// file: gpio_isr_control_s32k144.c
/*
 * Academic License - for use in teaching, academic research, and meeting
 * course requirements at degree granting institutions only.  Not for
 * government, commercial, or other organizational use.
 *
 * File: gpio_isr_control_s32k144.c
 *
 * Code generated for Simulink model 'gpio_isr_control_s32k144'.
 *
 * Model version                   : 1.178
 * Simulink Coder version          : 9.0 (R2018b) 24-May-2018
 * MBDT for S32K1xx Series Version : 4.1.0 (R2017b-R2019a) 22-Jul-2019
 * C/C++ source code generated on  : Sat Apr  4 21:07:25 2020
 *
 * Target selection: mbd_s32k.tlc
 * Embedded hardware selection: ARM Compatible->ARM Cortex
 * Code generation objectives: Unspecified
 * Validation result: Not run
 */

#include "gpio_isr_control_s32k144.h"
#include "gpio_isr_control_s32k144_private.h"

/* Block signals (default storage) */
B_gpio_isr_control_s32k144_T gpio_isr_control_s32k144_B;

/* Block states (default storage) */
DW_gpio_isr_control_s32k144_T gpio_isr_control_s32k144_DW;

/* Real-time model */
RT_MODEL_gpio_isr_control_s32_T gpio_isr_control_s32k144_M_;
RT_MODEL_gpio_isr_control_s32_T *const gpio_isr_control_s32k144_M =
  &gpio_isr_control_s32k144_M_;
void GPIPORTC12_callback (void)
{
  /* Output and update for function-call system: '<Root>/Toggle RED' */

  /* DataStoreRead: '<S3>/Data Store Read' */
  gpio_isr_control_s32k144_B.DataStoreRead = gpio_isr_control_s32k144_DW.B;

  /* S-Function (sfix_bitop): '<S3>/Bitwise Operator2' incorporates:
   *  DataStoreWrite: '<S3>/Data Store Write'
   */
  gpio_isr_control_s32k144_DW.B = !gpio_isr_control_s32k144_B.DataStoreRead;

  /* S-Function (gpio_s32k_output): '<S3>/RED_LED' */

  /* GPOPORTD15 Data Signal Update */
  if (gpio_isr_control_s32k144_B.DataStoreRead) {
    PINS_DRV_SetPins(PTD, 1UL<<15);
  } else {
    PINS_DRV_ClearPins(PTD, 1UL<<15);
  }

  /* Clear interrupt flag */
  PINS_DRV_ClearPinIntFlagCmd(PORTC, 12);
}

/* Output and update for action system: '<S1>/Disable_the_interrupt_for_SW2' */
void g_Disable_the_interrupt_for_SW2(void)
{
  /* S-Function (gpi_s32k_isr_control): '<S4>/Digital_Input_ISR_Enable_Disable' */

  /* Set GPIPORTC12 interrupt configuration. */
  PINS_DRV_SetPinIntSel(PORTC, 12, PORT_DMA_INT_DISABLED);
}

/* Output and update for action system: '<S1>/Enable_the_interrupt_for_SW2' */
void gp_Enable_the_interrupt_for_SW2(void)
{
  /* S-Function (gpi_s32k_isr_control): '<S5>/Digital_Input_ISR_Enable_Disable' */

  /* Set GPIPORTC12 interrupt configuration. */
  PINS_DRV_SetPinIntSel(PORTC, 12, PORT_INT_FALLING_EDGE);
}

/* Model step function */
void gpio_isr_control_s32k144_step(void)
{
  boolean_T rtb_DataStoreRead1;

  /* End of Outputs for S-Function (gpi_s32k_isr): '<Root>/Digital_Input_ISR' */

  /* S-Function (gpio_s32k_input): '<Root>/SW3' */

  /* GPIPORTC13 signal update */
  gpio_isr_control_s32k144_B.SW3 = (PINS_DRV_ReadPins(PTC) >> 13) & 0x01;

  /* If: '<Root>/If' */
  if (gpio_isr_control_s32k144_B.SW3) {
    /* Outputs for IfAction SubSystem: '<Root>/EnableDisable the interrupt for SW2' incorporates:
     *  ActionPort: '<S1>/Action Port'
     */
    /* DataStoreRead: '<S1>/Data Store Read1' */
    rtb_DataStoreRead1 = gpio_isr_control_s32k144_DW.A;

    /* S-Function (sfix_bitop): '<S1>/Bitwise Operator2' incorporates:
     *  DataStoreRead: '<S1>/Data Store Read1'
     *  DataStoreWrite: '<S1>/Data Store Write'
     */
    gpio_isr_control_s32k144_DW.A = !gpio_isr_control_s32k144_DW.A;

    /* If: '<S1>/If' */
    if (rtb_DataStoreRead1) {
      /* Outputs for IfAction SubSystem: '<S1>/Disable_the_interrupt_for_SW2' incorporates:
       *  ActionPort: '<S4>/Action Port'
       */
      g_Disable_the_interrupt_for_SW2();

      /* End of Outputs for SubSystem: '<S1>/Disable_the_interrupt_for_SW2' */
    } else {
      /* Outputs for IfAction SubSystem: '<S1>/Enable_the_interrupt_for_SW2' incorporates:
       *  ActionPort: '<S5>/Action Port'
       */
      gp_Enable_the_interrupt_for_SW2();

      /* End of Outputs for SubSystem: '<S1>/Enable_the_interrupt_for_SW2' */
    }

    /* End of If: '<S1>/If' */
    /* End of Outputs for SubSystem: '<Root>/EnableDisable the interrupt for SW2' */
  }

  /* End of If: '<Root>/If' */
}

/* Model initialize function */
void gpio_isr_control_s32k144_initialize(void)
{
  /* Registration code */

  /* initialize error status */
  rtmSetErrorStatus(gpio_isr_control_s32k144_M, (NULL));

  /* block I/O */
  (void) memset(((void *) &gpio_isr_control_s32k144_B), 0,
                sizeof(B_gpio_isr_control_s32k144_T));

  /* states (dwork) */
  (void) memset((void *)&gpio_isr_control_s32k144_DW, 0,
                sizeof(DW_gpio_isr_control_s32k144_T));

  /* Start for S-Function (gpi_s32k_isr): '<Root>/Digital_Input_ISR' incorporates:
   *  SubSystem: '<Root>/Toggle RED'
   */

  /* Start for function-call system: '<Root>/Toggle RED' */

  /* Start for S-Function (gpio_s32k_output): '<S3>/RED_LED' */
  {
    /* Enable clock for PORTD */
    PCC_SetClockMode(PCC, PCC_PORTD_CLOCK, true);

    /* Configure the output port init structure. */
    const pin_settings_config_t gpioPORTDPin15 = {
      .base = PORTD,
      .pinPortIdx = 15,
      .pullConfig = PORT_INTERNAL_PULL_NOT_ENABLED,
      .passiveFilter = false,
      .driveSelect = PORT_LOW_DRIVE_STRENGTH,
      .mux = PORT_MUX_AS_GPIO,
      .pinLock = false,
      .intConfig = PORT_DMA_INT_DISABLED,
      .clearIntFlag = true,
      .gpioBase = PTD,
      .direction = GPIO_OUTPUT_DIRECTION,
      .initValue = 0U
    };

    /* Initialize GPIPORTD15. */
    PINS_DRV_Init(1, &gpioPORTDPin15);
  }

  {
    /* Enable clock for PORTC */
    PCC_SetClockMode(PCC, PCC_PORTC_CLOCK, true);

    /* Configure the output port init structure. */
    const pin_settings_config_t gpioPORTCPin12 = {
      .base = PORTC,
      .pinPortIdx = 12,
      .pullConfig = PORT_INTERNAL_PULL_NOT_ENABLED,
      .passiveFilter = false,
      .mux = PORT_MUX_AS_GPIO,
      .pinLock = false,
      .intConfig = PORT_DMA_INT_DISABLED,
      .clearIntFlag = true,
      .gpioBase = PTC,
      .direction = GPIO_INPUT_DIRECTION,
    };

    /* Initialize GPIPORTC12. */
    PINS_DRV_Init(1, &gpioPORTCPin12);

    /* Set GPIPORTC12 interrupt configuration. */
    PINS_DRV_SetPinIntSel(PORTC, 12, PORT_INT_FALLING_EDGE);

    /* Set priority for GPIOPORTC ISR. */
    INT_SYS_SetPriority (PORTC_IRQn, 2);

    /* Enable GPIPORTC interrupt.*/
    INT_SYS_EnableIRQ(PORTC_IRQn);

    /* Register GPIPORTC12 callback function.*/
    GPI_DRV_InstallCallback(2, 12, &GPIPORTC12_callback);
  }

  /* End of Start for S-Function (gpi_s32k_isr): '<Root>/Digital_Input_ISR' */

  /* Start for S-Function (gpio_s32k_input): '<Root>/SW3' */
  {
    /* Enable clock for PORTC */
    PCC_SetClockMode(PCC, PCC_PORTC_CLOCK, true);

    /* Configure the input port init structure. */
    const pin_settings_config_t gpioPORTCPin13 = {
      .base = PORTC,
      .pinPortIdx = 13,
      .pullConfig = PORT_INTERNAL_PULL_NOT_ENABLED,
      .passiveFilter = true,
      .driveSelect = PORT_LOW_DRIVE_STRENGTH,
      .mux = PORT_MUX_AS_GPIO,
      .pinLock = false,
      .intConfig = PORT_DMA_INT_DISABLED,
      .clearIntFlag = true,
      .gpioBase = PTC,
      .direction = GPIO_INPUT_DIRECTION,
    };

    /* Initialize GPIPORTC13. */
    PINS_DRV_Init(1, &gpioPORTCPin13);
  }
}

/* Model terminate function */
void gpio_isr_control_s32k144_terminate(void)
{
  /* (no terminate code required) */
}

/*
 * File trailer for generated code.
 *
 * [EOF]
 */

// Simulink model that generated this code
simulink model "gpio_isr_control_s32k144"  (Simulink 9.2)
settings: Solver=FixedStepDiscrete  StartTime=0.0  StopTime=10.0  FixedStep=0.1  RelTol=1e-3  EnableMultiTasking=on
InitFcn:
  | mbd_s32k_consistency_checks(bdroot(gcs));
undefined symbols (not defined in the file): LQFP
libraries: mbd_s32k1xx_ec_toolbox x6, simulink x3

== system gpio_isr_control_s32k144 ==
  note: Toggle the Red LED
  note: Enable/Disable the interrupt for SW2
  note: Configuration
  Data Store Memory : DataStoreMemory  DataStoreName=B  ReadBeforeWriteMsg=warning  WriteAfterWriteMsg=warning  WriteAfterReadMsg=warning  ShowAdditionalParam=off  OutDataTypeStr=boolean
  Data Store Memory1 : DataStoreMemory  ReadBeforeWriteMsg=warning  WriteAfterWriteMsg=warning  WriteAfterReadMsg=warning  ShowAdditionalParam=off  OutDataTypeStr=boolean
  Digital_Input_ISR : mbd_s32k1xx_ec_toolbox/GPIO Blocks/Digital_Input_ISR  gpio_pin=PTC12: [PTC12 | Port C I/O]  irqc=on falling-edge  prio=2
  EnableDisable the interrupt for SW2 : Subsystem  TreatAsAtomicUnit=on
  If : If  IfExpression=u1 == 1  ShowElse=off
  MBD_S32K14x_Config_Information : mbd_s32k1xx_ec_toolbox/MBD_S32K1xx_Config_Information  mbdt_ver=0  disp_str=|  config_params=[]  mcu_target_name=S32K144  mcu_target_package=100-LQFP  mcu_target_sram_size=64KB  mcu_system_clock_freq=80  mcu_xtal_freq=External 8  mcu_steptick_timer=LPIT Channel 0  mcu_steptick_prio=15  ds_import_enable=on  target_compiler=GCC  target_memory=FLASH  gcc_target_compile_opts=-mcpu=cortex-m4 -mthumb -mfloat-abi=hard -mfpu=fpv4-sp-d16 -O1 -g -gstrict-dwarf  gcc_target_assemble_opts=-mcpu=cortex-m4 -mthumb -mfloat-abi=hard -mfpu=fpv4-sp-d16 -g  gcc_target_link_opts=-mcpu=cortex-m4 -mthumb -mfloat-abi=hard -mfpu=fpv4-sp-d16  gcc_target_default_lcf=on  gcc_target_user_lcf=S32K144_64_flash.ld  ghs_target_compile_opts=-cpu=cortexm4f -thumb -DARM_MATH_CM4 -fpu=vfpv4_d16 -fsingle -Ogeneral -Wundef -Wimplicit-int -Wshadow -Wtrigraphs --no_commons --gnu_asm -gnu99 -gdwarf-2 -G  ghs_target_assemble_opts=-cpu=cortexm4f -fpu=vfpv4_d16  ghs_target_link_opts=-cpu=cortexm4f -thumb -fpu=vfpv4_d16  ghs_target_default_lcf=on  ghs_target_user_lcf=S32K144_64_flash.ld  iar_target_compile_opts=--cpu=Cortex-M4F --thumb --fpu=VFPv4_sp -Ol -e --debug --dlib_config normal  iar_target_assemble_opts=--cpu Cortex-M4F --thumb --fpu VFPv4_sp  iar_target_link_opts=--no_exceptions --vfe --inline  iar_target_default_lcf=on  iar_target_user_lcf=S32K144_64_flash.icf  pil_download_enable=off  rbl_download_enable=on  rbl_start_delay=5000000  rbl_download_interface=OpenSDA  rbl_restart_request=off  rbl_com_port=Custom  rbl_com_port_custom=COM1  pil_download_rate=57600  pil_opensda_drive=Custom  pil_opensda_drive_custom=D  pil_uart_instance=1  pil_uart_rx=PTC6: [LPUART1_RX | Receive]  pil_uart_tx=PTC7: [LPUART1_TX | Transmit]  FTM_PWM_PcrCheckEnDis=on  FTM_Input_Edge_Inputs_PcrCheckEnDis=on  FTM_Dual_Edge_Inputs_PcrCheckEnDis=on  FTM_Quadrature_Inputs_PcrCheckEnDis=on  FTM_Hall_Sensor_Inputs_PcrCheckEnDis=on  LPTMR_PcrCheckEnDis=on  PIT_PcrCheckEnDis=on  RTC_PcrCheckEnDis=on  FlexCAN_PcrCheckEnDis=on  LIN_PcrCheckEnDis=on  FlexIO_PcrCheckEnDis=on  LPI2C_PcrCheckEnDis=on  LPSPI_PcrCheckEnDis=on  LPUART_PcrCheckEnDis=on  CMP_PcrCheckEnDis=on  GPIO_OutputPcrCheckEnDis=on  GPIO_InputPcrCheckEnDis=on  SBC_PcrCheckEnDis=on  AMMCLIB_PcrCheckEnDis=on  FM_PcrCheckEnDis=on  Profile_PcrCheckEnDis=on  ConfigParams_PcrCheckEnDis=on  ModelRef_PcrCheckEnDis=on  PDB0_PcrCheckEnDis=on  CSEc_PcrCheckEnDis=on  eDMA_PcrCheckEnDis=on  ADC_PcrCheckEnDis=on  WDOG_PcrCheckEnDis=on
      | Target : S32K144-64KB_SRAM
      | Package : 100-pin
      | System clock : 80 MHz
      | XTAL clock : External 8 MHz
      | Compiler : IAR
      | Target Type : FLASH
      | Download Code after build : off
      | Step Tick Interrupt Priority : 15
  Model Info1 : simulink/Model-Wide Utilities/Model Info  Frame=on  DisplayStringWithTags=|  HorizontalTextAlignment=Left  LeftAlignmentValue=0.02
      | Model Name: %<ModelName>
      | 
      | Description: %<Description>
  SW3 : mbd_s32k1xx_ec_toolbox/GPIO Blocks/Digital_Input  gpio_pin=PTC13: [PTC13 | Port C I/O]  pull_resistor=None  passive_filter=on
  Toggle RED : Subsystem  TreatAsAtomicUnit=on
  wires:
  Digital_Input_ISR/1 -> Toggle RED/Trigger
  SW3/1 -> If/1
  If/1 -> EnableDisable the interrupt for SW2/Action

== system gpio_isr_control_s32k144/EnableDisable the interrupt for SW2 ==
  Action Port : ActionPort  ActionType=then
  Bitwise Operator2 : simulink/Logic and Bit Operations/Bitwise Operator  logicop=NOT  UseBitMask=off  BitMask=bin2dec('11011001')  BitMaskRealWorld=Stored Integer
  Data Store Read1 : DataStoreRead
  Data Store Write : DataStoreWrite
  Disable_the_interrupt_for_SW2 : Subsystem
  Enable_the_interrupt_for_SW2 : Subsystem
  If : If  IfExpression=u1 == 1
  wires:
  Data Store Read1/1 -> Bitwise Operator2/1, If/1
  Bitwise Operator2/1 -> Data Store Write/1
  If/2 -> Enable_the_interrupt_for_SW2/Action
  If/1 -> Disable_the_interrupt_for_SW2/Action

== system gpio_isr_control_s32k144/Toggle RED ==
  Trigger : TriggerPort  TriggerType=function-call  VariantControl=Variant
  Bitwise Operator2 : simulink/Logic and Bit Operations/Bitwise Operator  logicop=NOT  UseBitMask=off  BitMask=bin2dec('11011001')  BitMaskRealWorld=Stored Integer
  Data Store Read : DataStoreRead  DataStoreName=B
  Data Store Write : DataStoreWrite  DataStoreName=B
  RED_LED : mbd_s32k1xx_ec_toolbox/GPIO Blocks/Digital_Output  gpio_pin=PTD15: [PTD15 | Port D I/O]  init_val=Low  drive_strength=Low
  wires:
  Bitwise Operator2/1 -> Data Store Write/1
  Data Store Read/1 -> RED_LED/1, Bitwise Operator2/1

== system gpio_isr_control_s32k144/EnableDisable the interrupt for SW2/Disable_the_interrupt_for_SW2 ==
  Action Port : ActionPort  ActionType=then
  Digital_Input_ISR_Enable_Disable : mbd_s32k1xx_ec_toolbox/GPIO Blocks/Digital_Input_ISR_Enable_Disable  gpio_pin=PTC12: [PTC12 | Port C I/O]  irqc=request disabled

== system gpio_isr_control_s32k144/EnableDisable the interrupt for SW2/Enable_the_interrupt_for_SW2 ==
  Action Port : ActionPort  ActionType=else
  Digital_Input_ISR_Enable_Disable : mbd_s32k1xx_ec_toolbox/GPIO Blocks/Digital_Input_ISR_Enable_Disable  gpio_pin=PTC12: [PTC12 | Port C I/O]  irqc=on falling-edge
